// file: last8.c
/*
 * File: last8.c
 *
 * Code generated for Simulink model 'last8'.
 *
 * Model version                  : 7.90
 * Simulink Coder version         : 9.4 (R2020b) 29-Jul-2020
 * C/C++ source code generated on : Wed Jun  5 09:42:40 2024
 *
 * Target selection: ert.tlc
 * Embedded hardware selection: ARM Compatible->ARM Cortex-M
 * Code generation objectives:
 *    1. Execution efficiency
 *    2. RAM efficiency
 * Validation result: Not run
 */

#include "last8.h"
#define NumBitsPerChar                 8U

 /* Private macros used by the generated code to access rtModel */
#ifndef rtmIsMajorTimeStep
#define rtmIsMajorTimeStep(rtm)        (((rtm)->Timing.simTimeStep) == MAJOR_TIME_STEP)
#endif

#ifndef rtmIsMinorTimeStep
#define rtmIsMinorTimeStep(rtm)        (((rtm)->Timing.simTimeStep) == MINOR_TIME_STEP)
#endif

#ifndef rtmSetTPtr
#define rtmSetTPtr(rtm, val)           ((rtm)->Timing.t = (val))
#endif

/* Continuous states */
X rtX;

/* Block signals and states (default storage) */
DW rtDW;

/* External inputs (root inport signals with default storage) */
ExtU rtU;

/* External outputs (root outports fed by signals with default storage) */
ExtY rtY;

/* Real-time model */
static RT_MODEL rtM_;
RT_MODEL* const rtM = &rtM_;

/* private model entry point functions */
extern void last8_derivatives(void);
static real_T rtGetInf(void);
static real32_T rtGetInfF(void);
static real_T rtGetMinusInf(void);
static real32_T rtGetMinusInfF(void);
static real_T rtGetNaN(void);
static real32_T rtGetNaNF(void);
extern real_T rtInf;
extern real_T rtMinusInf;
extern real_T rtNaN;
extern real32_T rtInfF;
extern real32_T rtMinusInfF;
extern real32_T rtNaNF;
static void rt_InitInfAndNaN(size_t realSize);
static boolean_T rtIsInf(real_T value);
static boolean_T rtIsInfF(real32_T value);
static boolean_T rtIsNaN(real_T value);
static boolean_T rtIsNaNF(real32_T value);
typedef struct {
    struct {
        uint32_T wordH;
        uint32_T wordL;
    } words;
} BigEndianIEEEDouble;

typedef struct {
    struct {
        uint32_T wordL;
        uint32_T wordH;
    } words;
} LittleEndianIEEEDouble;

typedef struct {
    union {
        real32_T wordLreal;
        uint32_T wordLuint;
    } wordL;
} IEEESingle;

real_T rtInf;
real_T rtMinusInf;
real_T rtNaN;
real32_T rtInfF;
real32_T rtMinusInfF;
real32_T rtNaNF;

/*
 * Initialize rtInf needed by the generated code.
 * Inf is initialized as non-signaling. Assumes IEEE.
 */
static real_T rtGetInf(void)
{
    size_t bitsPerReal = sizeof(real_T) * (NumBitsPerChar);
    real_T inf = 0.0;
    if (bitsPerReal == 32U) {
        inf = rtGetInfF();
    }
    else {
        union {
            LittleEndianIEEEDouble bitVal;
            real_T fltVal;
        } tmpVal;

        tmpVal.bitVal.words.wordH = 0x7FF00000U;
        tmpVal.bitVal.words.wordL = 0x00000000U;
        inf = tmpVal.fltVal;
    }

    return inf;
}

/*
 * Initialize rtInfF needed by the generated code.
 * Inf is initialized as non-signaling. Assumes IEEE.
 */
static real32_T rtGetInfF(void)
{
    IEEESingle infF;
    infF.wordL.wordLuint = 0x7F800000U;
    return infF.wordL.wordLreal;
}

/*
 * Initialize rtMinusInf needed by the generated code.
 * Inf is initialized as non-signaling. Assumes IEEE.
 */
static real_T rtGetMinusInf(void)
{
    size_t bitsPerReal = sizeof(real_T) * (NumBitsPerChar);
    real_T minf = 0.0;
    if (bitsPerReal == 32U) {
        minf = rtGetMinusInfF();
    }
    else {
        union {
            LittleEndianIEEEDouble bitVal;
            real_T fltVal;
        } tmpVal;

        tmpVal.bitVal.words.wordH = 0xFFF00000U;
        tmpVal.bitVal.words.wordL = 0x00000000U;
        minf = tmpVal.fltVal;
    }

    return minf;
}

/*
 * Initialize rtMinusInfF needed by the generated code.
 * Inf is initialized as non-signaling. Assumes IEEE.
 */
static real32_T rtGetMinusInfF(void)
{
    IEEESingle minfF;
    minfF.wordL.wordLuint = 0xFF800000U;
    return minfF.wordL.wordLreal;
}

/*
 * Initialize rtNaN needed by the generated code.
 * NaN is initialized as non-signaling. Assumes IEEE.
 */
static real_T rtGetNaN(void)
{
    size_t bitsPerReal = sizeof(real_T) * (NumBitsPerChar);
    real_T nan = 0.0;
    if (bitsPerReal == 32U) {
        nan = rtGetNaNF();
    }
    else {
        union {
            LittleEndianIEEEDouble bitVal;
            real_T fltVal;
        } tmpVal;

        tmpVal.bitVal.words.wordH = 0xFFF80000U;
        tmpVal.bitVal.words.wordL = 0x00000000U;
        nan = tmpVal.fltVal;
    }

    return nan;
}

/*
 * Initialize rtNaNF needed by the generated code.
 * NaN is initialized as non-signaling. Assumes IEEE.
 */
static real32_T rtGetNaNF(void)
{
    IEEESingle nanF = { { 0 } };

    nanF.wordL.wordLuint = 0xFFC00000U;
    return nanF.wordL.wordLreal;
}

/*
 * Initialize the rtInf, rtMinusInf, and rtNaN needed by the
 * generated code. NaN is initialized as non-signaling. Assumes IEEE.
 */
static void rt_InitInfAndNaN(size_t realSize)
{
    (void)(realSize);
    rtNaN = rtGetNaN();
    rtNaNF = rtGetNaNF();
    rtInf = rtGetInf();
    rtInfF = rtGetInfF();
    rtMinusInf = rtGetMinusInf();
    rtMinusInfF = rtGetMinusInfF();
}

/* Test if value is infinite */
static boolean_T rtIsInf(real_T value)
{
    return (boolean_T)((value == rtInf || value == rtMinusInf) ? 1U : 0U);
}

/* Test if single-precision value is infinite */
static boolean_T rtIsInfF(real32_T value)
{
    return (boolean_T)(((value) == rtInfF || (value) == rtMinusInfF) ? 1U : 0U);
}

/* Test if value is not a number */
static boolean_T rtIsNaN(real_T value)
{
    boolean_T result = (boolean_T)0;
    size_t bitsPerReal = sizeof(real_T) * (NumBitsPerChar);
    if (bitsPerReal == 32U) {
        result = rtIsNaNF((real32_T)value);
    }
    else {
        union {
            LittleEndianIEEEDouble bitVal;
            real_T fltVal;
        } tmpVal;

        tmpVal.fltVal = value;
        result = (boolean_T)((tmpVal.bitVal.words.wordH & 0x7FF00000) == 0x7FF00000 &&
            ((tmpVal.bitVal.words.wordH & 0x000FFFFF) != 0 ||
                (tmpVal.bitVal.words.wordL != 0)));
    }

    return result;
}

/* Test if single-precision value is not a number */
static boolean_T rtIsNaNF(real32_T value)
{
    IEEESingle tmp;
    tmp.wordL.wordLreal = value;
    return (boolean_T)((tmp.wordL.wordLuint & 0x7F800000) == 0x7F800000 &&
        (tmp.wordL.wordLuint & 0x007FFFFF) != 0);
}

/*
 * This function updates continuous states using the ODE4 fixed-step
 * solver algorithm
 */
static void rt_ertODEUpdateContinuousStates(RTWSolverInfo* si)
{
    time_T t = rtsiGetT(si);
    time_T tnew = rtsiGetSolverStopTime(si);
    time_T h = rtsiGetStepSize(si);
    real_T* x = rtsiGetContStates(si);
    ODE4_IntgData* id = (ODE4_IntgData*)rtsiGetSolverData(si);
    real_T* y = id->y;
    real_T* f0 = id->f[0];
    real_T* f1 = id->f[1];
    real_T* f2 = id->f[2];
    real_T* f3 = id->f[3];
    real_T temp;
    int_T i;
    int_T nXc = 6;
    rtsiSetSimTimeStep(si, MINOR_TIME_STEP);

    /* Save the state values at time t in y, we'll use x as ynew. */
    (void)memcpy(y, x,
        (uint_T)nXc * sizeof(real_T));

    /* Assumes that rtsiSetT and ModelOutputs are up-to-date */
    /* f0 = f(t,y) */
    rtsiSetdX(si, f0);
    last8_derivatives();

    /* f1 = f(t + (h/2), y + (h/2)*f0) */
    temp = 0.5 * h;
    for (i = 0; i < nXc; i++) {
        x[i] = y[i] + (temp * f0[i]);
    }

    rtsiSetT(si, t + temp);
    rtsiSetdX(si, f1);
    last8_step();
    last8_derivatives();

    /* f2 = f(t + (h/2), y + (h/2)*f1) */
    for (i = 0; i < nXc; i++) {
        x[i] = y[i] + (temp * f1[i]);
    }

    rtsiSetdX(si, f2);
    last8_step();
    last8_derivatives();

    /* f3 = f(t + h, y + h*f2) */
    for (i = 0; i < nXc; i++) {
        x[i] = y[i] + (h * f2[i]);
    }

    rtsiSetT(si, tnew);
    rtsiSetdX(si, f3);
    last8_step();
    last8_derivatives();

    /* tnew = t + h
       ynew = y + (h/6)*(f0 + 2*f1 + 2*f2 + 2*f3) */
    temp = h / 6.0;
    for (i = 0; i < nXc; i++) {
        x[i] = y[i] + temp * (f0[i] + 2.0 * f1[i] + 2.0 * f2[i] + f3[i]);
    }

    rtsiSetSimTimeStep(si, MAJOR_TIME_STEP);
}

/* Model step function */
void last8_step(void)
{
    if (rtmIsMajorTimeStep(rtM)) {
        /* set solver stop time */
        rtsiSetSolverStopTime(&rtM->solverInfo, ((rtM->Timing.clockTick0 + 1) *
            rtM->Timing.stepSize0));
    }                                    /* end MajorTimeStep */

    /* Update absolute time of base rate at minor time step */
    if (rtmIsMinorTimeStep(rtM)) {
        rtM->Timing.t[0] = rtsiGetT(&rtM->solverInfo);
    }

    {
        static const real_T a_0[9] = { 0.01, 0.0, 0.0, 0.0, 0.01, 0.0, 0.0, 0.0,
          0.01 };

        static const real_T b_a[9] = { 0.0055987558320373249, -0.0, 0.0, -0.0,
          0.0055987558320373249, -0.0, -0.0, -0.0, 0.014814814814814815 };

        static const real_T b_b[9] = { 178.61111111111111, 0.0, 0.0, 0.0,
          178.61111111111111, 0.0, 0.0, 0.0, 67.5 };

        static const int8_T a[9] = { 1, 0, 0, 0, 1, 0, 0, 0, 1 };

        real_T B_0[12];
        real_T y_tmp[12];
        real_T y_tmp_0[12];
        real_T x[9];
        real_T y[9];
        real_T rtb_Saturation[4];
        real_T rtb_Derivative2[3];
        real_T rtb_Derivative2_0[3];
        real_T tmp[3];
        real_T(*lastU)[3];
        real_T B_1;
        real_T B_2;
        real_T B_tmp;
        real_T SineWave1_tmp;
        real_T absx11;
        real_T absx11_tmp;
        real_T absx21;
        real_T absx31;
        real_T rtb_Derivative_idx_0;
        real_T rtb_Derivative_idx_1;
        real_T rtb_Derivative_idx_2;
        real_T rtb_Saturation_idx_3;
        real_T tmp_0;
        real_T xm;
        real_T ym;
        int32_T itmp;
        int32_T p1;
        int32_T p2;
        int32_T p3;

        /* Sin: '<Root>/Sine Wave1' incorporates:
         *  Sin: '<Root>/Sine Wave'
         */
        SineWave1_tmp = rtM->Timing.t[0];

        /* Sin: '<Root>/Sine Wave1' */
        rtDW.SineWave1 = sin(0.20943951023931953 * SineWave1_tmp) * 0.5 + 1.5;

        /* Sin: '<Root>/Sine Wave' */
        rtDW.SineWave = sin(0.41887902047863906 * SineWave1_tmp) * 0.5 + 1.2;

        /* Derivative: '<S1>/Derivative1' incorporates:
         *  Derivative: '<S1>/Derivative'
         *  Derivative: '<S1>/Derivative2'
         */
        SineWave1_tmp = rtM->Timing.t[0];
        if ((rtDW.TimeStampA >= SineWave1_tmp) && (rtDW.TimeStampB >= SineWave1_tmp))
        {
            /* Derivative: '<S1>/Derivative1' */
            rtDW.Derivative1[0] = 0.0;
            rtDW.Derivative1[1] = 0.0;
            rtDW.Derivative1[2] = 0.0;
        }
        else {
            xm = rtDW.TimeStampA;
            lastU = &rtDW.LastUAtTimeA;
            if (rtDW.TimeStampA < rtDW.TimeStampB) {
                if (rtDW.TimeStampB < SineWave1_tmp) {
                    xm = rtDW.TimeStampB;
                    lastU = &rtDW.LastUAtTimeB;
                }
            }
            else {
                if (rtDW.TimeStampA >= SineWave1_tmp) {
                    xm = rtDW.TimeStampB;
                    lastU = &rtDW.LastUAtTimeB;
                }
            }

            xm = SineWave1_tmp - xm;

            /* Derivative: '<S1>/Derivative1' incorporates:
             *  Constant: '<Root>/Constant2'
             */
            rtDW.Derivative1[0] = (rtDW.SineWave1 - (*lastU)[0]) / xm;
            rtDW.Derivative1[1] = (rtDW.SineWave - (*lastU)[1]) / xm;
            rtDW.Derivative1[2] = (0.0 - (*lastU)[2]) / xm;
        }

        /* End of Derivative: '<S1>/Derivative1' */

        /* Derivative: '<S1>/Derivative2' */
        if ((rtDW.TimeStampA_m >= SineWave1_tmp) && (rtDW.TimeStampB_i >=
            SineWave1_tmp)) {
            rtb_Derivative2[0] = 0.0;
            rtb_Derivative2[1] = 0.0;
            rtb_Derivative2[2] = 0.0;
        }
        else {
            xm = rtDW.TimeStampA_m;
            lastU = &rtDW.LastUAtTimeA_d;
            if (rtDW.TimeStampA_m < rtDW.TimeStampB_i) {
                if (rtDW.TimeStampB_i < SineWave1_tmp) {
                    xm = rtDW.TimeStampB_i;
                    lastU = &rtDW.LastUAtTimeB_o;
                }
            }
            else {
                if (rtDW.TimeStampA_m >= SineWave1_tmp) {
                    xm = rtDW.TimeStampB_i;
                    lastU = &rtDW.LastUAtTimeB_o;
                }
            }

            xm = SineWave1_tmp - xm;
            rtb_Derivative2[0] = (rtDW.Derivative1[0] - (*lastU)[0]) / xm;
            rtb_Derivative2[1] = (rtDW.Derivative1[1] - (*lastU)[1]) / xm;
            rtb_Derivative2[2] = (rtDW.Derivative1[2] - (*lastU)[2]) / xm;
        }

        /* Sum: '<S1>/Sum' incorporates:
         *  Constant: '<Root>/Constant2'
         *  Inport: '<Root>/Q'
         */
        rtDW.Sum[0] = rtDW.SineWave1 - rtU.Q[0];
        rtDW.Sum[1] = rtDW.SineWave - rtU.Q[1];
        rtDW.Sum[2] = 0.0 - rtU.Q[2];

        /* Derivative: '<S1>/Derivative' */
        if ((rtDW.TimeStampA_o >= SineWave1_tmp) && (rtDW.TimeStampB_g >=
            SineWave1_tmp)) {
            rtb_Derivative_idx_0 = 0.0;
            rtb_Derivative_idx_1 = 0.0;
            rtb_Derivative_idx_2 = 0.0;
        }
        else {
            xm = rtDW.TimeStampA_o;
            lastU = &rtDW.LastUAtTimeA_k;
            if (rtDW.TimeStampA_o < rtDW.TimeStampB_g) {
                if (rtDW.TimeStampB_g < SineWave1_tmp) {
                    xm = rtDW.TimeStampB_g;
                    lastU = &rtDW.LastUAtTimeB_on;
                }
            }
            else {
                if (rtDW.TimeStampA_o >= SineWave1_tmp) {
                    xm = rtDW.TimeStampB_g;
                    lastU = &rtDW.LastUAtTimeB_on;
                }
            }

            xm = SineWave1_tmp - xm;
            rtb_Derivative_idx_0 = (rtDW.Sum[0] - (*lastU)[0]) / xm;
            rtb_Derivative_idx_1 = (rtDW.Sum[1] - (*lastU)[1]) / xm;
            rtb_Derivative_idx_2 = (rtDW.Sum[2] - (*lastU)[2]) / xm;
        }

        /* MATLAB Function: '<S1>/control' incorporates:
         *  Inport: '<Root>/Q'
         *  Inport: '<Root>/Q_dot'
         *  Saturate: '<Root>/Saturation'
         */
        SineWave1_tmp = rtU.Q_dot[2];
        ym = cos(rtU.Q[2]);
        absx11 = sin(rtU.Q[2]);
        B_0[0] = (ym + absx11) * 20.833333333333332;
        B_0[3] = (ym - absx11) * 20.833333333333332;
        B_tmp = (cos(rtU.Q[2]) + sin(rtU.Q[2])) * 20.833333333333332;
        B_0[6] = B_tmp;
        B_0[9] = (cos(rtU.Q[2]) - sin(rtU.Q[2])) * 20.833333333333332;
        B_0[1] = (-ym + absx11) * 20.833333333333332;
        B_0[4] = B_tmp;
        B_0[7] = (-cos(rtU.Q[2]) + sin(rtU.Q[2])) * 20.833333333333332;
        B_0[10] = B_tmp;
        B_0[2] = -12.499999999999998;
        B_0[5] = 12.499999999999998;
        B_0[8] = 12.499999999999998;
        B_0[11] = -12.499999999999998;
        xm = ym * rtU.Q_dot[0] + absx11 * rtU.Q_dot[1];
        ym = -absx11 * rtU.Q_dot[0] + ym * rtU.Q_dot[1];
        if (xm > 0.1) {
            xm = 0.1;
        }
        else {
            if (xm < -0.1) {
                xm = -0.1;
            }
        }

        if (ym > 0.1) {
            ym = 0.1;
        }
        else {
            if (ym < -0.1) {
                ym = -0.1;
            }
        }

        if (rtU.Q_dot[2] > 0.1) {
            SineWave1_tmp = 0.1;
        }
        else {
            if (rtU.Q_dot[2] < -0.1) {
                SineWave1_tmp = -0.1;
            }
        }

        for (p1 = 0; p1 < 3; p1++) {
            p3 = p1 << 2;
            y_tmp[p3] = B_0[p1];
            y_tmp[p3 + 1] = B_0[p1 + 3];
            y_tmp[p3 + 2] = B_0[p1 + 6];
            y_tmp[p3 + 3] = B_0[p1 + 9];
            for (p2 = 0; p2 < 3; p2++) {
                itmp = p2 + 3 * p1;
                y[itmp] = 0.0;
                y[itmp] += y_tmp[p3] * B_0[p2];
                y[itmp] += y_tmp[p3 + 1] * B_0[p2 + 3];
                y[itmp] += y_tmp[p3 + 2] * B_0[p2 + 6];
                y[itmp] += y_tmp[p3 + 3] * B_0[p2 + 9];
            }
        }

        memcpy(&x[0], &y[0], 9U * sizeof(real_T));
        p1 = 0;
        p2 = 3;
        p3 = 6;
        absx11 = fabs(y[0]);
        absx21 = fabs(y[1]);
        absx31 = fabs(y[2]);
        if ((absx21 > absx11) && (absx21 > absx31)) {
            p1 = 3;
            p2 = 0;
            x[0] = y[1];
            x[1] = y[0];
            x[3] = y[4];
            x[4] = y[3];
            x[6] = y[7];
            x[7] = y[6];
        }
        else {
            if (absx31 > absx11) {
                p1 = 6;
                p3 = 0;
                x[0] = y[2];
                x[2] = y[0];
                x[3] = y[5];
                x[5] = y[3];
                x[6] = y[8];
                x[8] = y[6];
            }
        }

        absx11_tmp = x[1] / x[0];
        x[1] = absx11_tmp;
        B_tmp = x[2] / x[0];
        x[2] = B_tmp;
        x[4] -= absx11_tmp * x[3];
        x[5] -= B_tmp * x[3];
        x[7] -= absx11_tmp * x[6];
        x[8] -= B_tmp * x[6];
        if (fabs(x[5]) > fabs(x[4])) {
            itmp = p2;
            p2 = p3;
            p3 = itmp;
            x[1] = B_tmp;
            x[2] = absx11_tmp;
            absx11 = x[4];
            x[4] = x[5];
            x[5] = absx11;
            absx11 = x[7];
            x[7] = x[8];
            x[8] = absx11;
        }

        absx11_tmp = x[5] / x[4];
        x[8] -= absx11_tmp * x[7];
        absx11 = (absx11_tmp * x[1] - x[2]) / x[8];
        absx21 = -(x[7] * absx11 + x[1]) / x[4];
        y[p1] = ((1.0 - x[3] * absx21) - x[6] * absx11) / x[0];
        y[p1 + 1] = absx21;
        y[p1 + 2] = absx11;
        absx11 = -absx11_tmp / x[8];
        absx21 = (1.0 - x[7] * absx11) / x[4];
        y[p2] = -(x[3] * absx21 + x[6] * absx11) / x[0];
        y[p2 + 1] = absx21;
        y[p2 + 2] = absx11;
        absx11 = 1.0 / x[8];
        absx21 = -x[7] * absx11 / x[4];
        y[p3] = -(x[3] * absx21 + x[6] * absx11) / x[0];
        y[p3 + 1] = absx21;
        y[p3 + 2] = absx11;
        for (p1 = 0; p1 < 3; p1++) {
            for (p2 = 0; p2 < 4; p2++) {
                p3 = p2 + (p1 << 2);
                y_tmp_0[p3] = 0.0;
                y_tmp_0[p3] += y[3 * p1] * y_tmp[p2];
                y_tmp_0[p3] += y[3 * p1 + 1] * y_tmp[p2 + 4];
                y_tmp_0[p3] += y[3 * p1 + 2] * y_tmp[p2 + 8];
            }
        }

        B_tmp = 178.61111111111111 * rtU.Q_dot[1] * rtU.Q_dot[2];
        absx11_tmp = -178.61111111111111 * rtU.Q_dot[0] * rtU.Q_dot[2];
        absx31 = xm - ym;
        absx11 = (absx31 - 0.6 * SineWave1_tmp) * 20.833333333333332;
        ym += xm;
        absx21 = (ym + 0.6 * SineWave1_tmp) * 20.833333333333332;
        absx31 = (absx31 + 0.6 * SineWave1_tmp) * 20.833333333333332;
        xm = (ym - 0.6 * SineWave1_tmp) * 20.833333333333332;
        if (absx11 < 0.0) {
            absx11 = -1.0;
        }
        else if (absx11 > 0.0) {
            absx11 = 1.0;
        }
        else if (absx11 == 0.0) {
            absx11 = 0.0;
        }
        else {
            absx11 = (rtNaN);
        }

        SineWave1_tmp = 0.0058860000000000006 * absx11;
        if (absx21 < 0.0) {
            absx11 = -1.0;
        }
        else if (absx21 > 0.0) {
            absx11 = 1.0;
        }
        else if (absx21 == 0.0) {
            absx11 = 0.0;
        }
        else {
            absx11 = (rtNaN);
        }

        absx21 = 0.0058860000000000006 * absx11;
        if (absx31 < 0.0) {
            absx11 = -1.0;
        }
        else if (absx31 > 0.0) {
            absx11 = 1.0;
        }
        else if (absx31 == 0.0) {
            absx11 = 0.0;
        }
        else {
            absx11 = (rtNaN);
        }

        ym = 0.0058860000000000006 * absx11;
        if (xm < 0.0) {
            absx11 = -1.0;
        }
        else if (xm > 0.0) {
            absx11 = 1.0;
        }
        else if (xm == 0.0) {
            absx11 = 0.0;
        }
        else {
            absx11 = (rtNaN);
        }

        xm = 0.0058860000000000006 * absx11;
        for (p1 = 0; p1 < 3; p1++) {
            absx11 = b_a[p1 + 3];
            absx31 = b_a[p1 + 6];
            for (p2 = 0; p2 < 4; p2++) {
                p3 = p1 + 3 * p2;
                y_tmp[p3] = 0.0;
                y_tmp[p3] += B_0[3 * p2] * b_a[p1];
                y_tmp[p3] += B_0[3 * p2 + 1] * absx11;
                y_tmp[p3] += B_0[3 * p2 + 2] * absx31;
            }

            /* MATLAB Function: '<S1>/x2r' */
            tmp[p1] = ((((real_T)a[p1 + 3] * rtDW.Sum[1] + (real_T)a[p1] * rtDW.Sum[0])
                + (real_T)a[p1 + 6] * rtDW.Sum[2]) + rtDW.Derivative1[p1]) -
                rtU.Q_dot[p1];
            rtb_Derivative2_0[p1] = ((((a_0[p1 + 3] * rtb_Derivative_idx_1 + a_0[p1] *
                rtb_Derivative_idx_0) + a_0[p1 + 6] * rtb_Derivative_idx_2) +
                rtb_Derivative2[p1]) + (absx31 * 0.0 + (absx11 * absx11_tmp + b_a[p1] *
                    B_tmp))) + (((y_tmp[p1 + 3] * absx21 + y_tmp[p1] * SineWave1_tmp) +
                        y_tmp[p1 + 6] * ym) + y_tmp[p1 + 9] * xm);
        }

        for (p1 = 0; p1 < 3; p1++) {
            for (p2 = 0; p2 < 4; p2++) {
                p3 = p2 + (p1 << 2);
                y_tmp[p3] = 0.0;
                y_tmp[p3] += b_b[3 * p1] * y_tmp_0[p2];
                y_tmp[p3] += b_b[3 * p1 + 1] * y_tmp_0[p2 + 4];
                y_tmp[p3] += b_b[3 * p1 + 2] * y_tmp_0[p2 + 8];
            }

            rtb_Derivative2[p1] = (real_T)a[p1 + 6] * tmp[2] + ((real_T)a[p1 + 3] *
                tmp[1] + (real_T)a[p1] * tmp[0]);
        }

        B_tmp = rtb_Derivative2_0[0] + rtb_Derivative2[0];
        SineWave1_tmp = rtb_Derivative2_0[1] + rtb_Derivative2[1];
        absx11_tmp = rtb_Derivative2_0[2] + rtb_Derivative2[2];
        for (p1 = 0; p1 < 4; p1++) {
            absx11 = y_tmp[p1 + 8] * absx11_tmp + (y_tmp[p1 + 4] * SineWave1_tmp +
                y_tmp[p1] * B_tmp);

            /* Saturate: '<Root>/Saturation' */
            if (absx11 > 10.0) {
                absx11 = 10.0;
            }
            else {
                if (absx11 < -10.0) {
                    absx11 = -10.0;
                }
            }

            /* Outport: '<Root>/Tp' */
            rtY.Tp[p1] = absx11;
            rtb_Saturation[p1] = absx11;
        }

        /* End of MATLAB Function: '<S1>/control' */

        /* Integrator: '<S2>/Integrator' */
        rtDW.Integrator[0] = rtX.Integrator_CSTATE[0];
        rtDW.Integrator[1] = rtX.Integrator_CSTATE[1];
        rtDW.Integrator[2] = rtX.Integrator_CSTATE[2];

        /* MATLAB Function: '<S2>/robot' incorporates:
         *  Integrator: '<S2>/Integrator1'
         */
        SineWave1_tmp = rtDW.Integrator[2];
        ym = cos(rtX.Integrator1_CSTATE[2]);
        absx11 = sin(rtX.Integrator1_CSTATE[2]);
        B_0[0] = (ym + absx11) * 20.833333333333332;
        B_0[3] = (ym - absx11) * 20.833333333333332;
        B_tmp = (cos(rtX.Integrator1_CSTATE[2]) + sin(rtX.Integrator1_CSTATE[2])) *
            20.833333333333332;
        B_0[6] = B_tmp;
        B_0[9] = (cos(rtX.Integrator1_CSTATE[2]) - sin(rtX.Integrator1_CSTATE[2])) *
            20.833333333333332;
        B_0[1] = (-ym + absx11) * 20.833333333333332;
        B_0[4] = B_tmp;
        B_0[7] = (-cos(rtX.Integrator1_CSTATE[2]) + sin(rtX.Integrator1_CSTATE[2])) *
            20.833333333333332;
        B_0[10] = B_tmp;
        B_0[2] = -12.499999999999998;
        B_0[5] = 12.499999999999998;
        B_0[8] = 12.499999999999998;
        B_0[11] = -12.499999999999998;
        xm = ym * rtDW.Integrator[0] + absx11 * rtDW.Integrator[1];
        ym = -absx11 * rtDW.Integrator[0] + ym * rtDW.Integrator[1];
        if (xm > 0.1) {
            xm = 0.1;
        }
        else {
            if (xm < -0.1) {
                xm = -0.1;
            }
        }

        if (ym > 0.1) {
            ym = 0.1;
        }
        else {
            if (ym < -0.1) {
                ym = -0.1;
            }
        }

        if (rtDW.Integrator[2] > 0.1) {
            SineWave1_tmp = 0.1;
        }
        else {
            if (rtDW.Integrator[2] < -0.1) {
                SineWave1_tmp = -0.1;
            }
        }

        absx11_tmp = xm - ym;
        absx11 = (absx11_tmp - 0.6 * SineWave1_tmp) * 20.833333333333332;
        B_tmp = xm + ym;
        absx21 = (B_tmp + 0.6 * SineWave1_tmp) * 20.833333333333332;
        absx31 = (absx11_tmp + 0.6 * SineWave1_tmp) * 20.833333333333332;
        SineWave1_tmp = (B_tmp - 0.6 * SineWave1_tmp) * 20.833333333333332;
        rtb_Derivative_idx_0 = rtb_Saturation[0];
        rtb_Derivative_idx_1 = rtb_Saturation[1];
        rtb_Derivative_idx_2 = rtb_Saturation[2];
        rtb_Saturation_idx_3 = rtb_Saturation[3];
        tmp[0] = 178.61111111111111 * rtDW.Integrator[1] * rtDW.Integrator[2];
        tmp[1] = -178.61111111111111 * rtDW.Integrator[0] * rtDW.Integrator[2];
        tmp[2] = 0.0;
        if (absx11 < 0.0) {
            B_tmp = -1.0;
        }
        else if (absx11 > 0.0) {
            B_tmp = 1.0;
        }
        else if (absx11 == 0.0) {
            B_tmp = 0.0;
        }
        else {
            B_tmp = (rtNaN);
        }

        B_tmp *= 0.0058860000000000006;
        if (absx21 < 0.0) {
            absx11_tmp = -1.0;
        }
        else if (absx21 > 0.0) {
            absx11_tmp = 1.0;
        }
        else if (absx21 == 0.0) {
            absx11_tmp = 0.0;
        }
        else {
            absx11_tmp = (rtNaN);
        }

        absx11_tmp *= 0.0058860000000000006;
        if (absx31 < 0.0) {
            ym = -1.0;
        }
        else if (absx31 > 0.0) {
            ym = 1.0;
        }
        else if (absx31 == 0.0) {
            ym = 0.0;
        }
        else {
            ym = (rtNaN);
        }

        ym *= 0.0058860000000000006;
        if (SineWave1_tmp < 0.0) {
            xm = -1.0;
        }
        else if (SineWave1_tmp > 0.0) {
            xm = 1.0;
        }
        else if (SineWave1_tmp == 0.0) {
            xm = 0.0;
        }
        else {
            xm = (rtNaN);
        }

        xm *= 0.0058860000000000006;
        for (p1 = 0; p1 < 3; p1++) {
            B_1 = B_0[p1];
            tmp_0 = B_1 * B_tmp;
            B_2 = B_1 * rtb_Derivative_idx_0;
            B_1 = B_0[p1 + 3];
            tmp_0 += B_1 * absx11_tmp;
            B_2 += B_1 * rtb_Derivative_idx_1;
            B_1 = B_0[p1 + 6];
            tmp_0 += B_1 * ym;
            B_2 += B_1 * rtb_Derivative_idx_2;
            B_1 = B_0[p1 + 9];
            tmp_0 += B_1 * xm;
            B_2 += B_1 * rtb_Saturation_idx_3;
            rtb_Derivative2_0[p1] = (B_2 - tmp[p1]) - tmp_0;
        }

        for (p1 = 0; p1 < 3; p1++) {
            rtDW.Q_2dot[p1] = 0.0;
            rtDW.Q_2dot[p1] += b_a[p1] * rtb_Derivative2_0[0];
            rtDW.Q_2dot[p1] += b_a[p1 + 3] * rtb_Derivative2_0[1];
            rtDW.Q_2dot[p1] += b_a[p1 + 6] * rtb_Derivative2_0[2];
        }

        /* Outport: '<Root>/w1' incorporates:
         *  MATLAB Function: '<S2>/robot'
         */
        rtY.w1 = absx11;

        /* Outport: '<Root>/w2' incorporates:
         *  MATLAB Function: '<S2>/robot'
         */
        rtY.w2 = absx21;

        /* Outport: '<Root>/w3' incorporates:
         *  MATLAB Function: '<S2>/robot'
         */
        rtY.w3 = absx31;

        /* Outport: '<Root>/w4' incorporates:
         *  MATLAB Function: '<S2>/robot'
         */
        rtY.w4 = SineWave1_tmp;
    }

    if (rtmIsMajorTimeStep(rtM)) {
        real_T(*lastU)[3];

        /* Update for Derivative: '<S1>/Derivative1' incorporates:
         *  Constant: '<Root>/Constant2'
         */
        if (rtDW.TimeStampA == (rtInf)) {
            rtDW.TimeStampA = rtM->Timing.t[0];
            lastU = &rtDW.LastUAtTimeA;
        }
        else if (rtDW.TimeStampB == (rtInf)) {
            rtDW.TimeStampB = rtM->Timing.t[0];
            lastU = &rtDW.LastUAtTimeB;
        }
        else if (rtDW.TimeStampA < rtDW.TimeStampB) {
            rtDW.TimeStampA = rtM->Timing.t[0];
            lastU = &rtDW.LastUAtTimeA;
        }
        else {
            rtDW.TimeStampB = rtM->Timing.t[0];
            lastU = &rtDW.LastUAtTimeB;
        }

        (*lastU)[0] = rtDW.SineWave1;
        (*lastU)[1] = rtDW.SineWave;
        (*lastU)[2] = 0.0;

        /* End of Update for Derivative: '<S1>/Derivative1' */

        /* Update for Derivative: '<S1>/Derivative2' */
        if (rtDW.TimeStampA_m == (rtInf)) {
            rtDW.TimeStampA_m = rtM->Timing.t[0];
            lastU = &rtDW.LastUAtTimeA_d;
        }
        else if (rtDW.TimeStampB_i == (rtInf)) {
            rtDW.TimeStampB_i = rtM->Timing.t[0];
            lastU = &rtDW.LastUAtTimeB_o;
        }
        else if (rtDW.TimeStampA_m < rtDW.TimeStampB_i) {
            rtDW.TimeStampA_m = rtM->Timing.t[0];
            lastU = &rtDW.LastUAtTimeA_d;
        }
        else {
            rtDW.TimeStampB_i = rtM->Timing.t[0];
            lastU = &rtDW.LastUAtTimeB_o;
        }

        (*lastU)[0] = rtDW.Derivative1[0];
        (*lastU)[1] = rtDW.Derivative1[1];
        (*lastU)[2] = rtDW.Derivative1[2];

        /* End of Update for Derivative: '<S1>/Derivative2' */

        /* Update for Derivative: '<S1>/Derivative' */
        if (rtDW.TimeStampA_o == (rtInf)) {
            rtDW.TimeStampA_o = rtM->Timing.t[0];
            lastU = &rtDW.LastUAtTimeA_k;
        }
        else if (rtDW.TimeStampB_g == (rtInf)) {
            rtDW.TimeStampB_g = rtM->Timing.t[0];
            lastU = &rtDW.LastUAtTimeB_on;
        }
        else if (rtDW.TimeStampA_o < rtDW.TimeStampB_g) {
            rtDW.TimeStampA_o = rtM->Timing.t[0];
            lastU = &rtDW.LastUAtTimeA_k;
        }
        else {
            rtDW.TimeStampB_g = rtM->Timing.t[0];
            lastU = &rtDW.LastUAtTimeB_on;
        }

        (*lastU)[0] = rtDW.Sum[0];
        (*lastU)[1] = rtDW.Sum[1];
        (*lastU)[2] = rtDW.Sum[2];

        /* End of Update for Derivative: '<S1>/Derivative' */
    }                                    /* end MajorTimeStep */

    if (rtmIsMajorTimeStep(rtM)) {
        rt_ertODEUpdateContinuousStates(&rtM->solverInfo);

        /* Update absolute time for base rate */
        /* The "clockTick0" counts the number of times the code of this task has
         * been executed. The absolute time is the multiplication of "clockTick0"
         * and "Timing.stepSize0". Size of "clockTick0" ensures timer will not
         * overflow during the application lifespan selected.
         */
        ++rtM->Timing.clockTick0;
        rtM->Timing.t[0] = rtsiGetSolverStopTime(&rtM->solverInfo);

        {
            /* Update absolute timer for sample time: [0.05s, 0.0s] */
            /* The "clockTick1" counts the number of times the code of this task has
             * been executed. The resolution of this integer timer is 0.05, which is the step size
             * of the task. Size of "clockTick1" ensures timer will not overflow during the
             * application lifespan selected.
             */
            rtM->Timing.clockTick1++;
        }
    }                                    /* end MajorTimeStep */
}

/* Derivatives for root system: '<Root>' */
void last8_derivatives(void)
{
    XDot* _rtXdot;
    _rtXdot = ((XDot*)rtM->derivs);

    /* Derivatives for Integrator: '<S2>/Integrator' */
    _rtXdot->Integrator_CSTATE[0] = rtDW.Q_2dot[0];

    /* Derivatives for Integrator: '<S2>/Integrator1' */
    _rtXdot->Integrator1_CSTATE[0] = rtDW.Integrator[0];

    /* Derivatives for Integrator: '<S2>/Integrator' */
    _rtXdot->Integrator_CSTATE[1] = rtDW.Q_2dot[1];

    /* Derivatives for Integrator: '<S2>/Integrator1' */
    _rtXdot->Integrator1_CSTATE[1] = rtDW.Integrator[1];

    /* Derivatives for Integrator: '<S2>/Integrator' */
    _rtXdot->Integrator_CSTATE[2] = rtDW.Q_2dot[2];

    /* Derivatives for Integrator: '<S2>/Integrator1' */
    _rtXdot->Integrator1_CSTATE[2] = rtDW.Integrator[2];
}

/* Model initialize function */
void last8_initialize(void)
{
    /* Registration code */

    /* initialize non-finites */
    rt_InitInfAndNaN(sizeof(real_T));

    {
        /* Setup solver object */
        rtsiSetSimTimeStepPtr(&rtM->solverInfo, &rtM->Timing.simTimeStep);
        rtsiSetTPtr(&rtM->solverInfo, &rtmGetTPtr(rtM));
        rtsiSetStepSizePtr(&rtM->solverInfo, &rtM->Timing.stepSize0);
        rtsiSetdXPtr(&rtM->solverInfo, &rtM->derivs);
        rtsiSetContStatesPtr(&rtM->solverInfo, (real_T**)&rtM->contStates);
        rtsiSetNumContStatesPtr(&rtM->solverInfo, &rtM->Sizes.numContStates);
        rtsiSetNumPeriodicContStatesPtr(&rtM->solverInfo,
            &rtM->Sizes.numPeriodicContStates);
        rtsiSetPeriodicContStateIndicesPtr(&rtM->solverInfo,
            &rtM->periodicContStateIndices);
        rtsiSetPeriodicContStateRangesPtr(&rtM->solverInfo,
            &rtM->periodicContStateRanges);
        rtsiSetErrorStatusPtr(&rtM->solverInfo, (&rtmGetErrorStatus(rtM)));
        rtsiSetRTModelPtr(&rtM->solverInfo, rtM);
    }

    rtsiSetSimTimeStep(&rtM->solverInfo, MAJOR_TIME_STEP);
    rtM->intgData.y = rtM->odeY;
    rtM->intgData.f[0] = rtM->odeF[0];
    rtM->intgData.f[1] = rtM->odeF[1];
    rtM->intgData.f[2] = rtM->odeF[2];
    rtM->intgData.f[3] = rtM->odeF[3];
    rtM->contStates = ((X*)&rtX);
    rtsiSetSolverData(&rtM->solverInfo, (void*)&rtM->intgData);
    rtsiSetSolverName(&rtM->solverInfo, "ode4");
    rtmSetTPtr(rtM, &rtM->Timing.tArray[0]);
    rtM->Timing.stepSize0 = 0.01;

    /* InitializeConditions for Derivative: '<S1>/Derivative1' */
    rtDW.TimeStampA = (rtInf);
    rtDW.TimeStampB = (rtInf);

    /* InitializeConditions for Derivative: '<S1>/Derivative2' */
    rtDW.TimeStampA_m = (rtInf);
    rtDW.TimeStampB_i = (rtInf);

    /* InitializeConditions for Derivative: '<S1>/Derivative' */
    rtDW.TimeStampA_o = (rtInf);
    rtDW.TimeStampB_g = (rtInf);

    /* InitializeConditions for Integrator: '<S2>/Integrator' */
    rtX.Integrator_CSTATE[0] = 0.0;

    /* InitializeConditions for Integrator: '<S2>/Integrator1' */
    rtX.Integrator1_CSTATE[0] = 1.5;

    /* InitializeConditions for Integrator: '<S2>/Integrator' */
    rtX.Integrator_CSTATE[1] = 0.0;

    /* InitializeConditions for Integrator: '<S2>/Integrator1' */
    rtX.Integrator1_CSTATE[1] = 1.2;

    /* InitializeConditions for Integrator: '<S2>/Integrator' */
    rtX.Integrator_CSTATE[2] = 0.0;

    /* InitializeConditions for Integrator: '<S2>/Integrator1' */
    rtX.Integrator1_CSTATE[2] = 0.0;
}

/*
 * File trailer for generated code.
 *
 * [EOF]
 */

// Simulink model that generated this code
simulink model "last8"  (R2020b)
settings: Solver=ode4  StartTime=0.0  StopTime=30  FixedStep=0.05  RelTol=1e-3

== system last8 ==
  Q : Inport  PortDimensions=3
  Q_dot : Inport  Port=2  PortDimensions=3
  CONTROL : Subsystem
  Constant2 : Constant  Value=0
  Mux : Mux  Inputs=3
  Physical Plant : Subsystem
  Saturation : Saturate  UpperLimit=10  LowerLimit=-10
  Sine Wave : Sin  Amplitude=0.5  Bias=1.2  Frequency=4*pi/30
  Sine Wave1 : Sin  Amplitude=0.5  Bias=1.5  Frequency=2*pi/30
  w1 : Outport  VectorParamsAs1DForOutWhenUnconnected=off
  w2 : Outport  Port=2  VectorParamsAs1DForOutWhenUnconnected=off
  w3 : Outport  Port=3  VectorParamsAs1DForOutWhenUnconnected=off
  w4 : Outport  Port=4  VectorParamsAs1DForOutWhenUnconnected=off
  Tp : Outport  Port=5  PortDimensions=4  VectorParamsAs1DForOutWhenUnconnected=off
  wires:
  Mux/1 -> CONTROL/1(Qr)
  CONTROL/1(u) -> Saturation/1
  Saturation/1 -> Tp/1, Physical Plant/1(T)
  Physical Plant/1(w1) -> w1/1
  Physical Plant/2(w2) -> w2/1
  Physical Plant/3(w3) -> w3/1
  Physical Plant/4(w4) -> w4/1
  Sine Wave1/1 -> Mux/1
  Sine Wave/1 -> Mux/2
  Constant2/1 -> Mux/3
  Q_dot/1 -> CONTROL/3(Q_dot)
  Q/1 -> CONTROL/2(Q)

== system last8/CONTROL ==
  Qr : Inport
  Q : Inport  Port=2  PortDimensions=3
  Q_dot : Inport  Port=3
  Demux : Demux  Outputs=3
  Demux1 : Demux  Outputs=3
  Derivative : Derivative
  Derivative1 : Derivative
  Derivative2 : Derivative
  Sum : Sum  Inputs=|+-
  control : MATLAB Function  TreatAsAtomicUnit=on
  x2r : MATLAB Function  TreatAsAtomicUnit=on
  u : Outport  VectorParamsAs1DForOutWhenUnconnected=off
  wires:
  Qr/1 -> Derivative1/1, Sum/1
  Derivative1/1 -> x2r/1(Qr_dot), Derivative2/1
  control/1(u_control) -> u/1
  Q/1 -> Sum/2, Demux1/1
  Q_dot/1 -> x2r/2(Q_dot), Demux/1
  Demux/3 -> control/6(theta_dot)
  Demux1/3 -> control/7(theta)
  Sum/1 -> x2r/3(e1), Derivative/1
  Derivative2/1 -> control/1(Qr_2dot)
  Derivative/1 -> control/2(e1_dot)
  x2r/1(e2) -> control/3(e2)
  Demux/1 -> control/4(x_dot)
  Demux/2 -> control/5(y_dot)

== system last8/Physical Plant ==
  T : Inport  PortDimensions=4
  Demux : Demux
  Demux1 : Demux  Outputs=3
  Demux2 : Demux  Outputs=3
  Integrator : Integrator
  Integrator1 : Integrator  InitialCondition=[1.5 1.2 0]
  robot : MATLAB Function  TreatAsAtomicUnit=on
  w1 : Outport  VectorParamsAs1DForOutWhenUnconnected=off
  w2 : Outport  Port=2  VectorParamsAs1DForOutWhenUnconnected=off
  w3 : Outport  Port=3  VectorParamsAs1DForOutWhenUnconnected=off
  w4 : Outport  Port=4  VectorParamsAs1DForOutWhenUnconnected=off
  wires:
  Demux/1 -> robot/1(T1)
  Demux/2 -> robot/2(T2)
  Demux/3 -> robot/3(T3)
  Demux/4 -> robot/4(T4)
  robot/1(Q_2dot) -> Integrator/1
  Demux1/3 -> robot/7(theta_dot)
  Integrator1/1 -> Demux2/1
  Demux2/3 -> robot/8(theta)
  T/1 -> Demux/1
  robot/2(w1) -> w1/1
  robot/3(w2) -> w2/1
  robot/4(w3) -> w3/1
  robot/5(w4) -> w4/1
  Integrator/1 -> Demux1/1, Integrator1/1
  Demux1/1 -> robot/5(x_dot)
  Demux1/2 -> robot/6(y_dot)

== matlab function last8/Physical Plant/robot ==
function [Q_2dot,w1,w2,w3,w4]  = fcn(T1, T2, T3, T4,x_dot,y_dot,theta_dot,theta)
m = 5;
I = 5;
Ib = 0.1;
l1 = 0.3;
l2 = 0.3;
r = 0.048;
g = 9.81;
u = 0.01;
N = m*g/4;
M =[(m+4*Ib/(r*r)) 0 0; 0 (m+4*Ib/(r*r)) 0; 0 0 (I+4*Ib*(l1+l2)*(l1+l2)/(r*r))];
C = [(m+4*Ib/(r*r))*y_dot*theta_dot;-(m+4*Ib/(r*r))*x_dot*theta_dot;0 ];
B = (1/r)*[(cos(theta)+sin(theta)) (cos(theta)-sin(theta)) (cos(theta)+sin(theta)) (cos(theta)-sin(theta));
         (-cos(theta)+sin(theta)) (cos(theta)+sin(theta)) (-cos(theta)+sin(theta)) (cos(theta)+sin(theta)); 
         (-(l1+l2)) (l1+l2) (l1+l2) (-(l1+l2))];
T = [T1;T2;T3;T4];

xm = cos(theta)*x_dot+sin(theta)*y_dot;
ym = -sin(theta)*x_dot+cos(theta)*y_dot;

v_max = 0.1;
if xm > v_max
    xm = v_max;
elseif xm < -v_max
    xm = -v_max;
end
if ym > v_max
    ym = v_max;
elseif ym < -v_max
    ym = -v_max;
end
if theta_dot > v_max
    theta_dot = v_max;
elseif theta_dot < -v_max
    theta_dot = -v_max;
end

w1 = (1/r)*(xm-ym-(l1+l2)*theta_dot);
w2 = (1/r)*(xm+ym+(l1+l2)*theta_dot);
w3 = (1/r)*(xm-ym+(l1+l2)*theta_dot);
w4 = (1/r)*(xm+ym-(l1+l2)*theta_dot);

% w_max = 2;
% if w1 > w_max
%     w1 = w_max;
% elseif w1 < -w_max
%     w1 = -w_max;
% end
% if w2 > w_max
%     w2 = w_max;
% elseif w2 < -w_max
%     w2 = -w_max;
% end
% if w3 > w_max
%     w3 = w_max;
% elseif w3 < -w_max
%     w3 = -w_max;
% end
% if w4 > w_max
%     w4 = w_max;
% elseif w4 < -w_max
%     w4 = -w_max;
% end

Xi=[u*r*N*sign(w1);u*r*N*sign(w2);u*r*N*sign(w3);u*N*r*sign(w4)];

Q_2dot=inv(M)*(B*T-C-B*Xi);

== matlab function last8/CONTROL/control ==
function u_control = fcn(Qr_2dot,e1_dot,e2,x_dot,y_dot,theta_dot,theta)

m = 5;
I = 5;
Ib = 0.1;
l1 = 0.3;
l2 = 0.3;
r = 0.048;
g = 9.81;
u = 0.01;
N = m*g/4;
M = [(m+4*Ib/(r*r)) 0 0; 0 (m+4*Ib/(r*r)) 0; 0 0 (I+4*Ib*(l1+l2)*(l1+l2)/(r*r))];
C = [(m+4*Ib/(r*r))*y_dot*theta_dot;-(m+4*Ib/(r*r))*x_dot*theta_dot;0 ];
B = (1/r)*[(cos(theta)+sin(theta)) (cos(theta)-sin(theta)) (cos(theta)+sin(theta)) (cos(theta)-sin(theta));
    (-cos(theta)+sin(theta)) (cos(theta)+sin(theta)) (-cos(theta)+sin(theta)) (cos(theta)+sin(theta)); 
    (-(l1+l2)) (l1+l2) (l1+l2) (-(l1+l2))];

xm = cos(theta)*x_dot+sin(theta)*y_dot;
ym = -sin(theta)*x_dot+cos(theta)*y_dot;

v_max = 0.1;
if xm > v_max
    xm = v_max;
elseif xm < -v_max
    xm = -v_max;
end
if ym > v_max
    ym = v_max;
elseif ym < -v_max
    ym = -v_max;
end
if theta_dot > v_max
    theta_dot = v_max;
elseif theta_dot < -v_max
    theta_dot = -v_max;
end

w1 = (1/r)*(xm-ym-(l1+l2)*theta_dot);
w2 = (1/r)*(xm+ym+(l1+l2)*theta_dot);
w3 = (1/r)*(xm-ym+(l1+l2)*theta_dot);
w4 = (1/r)*(xm+ym-(l1+l2)*theta_dot);

% w_max = 2;
% if w1 > w_max
%     w1 = w_max;
% elseif w1 < -w_max
%     w1 = -w_max;
% end
% if w2 > w_max
%     w2 = w_max;
% elseif w2 < -w_max
%     w2 = -w_max;
% end
% if w3 > w_max
%     w3 = w_max;
% elseif w3 < -w_max
%     w3 = -w_max;
% end
% if w4 > w_max
%     w4 = w_max;
% elseif w4 < -w_max
%     w4 = -w_max;
% end

Xi=[u*r*N*sign(w1);u*r*N*sign(w2);u*r*N*sign(w3);u*N*r*sign(w4)];

k1 = [0.01 0 0;
      0 0.01 0;
      0 0 0.01];
k2 = [1 0 0;
      0 1 0;
      0 0 1];
  
u_control = B'*inv(B*B')*M*((Qr_2dot+k1*e1_dot)+inv(M)*C+inv(M)*B*Xi+k2*e2);

== matlab function last8/CONTROL/x2r ==
function e2  = fcn(Qr_dot,Q_dot,e1)

k1 = [1 0 0;
      0 1 0;
      0 0 1];
 
%x2r_dot = (Qr_2dot+k1*e1_dot);
x2r = Qr_dot + k1*e1;
e2 = x2r - Q_dot;
